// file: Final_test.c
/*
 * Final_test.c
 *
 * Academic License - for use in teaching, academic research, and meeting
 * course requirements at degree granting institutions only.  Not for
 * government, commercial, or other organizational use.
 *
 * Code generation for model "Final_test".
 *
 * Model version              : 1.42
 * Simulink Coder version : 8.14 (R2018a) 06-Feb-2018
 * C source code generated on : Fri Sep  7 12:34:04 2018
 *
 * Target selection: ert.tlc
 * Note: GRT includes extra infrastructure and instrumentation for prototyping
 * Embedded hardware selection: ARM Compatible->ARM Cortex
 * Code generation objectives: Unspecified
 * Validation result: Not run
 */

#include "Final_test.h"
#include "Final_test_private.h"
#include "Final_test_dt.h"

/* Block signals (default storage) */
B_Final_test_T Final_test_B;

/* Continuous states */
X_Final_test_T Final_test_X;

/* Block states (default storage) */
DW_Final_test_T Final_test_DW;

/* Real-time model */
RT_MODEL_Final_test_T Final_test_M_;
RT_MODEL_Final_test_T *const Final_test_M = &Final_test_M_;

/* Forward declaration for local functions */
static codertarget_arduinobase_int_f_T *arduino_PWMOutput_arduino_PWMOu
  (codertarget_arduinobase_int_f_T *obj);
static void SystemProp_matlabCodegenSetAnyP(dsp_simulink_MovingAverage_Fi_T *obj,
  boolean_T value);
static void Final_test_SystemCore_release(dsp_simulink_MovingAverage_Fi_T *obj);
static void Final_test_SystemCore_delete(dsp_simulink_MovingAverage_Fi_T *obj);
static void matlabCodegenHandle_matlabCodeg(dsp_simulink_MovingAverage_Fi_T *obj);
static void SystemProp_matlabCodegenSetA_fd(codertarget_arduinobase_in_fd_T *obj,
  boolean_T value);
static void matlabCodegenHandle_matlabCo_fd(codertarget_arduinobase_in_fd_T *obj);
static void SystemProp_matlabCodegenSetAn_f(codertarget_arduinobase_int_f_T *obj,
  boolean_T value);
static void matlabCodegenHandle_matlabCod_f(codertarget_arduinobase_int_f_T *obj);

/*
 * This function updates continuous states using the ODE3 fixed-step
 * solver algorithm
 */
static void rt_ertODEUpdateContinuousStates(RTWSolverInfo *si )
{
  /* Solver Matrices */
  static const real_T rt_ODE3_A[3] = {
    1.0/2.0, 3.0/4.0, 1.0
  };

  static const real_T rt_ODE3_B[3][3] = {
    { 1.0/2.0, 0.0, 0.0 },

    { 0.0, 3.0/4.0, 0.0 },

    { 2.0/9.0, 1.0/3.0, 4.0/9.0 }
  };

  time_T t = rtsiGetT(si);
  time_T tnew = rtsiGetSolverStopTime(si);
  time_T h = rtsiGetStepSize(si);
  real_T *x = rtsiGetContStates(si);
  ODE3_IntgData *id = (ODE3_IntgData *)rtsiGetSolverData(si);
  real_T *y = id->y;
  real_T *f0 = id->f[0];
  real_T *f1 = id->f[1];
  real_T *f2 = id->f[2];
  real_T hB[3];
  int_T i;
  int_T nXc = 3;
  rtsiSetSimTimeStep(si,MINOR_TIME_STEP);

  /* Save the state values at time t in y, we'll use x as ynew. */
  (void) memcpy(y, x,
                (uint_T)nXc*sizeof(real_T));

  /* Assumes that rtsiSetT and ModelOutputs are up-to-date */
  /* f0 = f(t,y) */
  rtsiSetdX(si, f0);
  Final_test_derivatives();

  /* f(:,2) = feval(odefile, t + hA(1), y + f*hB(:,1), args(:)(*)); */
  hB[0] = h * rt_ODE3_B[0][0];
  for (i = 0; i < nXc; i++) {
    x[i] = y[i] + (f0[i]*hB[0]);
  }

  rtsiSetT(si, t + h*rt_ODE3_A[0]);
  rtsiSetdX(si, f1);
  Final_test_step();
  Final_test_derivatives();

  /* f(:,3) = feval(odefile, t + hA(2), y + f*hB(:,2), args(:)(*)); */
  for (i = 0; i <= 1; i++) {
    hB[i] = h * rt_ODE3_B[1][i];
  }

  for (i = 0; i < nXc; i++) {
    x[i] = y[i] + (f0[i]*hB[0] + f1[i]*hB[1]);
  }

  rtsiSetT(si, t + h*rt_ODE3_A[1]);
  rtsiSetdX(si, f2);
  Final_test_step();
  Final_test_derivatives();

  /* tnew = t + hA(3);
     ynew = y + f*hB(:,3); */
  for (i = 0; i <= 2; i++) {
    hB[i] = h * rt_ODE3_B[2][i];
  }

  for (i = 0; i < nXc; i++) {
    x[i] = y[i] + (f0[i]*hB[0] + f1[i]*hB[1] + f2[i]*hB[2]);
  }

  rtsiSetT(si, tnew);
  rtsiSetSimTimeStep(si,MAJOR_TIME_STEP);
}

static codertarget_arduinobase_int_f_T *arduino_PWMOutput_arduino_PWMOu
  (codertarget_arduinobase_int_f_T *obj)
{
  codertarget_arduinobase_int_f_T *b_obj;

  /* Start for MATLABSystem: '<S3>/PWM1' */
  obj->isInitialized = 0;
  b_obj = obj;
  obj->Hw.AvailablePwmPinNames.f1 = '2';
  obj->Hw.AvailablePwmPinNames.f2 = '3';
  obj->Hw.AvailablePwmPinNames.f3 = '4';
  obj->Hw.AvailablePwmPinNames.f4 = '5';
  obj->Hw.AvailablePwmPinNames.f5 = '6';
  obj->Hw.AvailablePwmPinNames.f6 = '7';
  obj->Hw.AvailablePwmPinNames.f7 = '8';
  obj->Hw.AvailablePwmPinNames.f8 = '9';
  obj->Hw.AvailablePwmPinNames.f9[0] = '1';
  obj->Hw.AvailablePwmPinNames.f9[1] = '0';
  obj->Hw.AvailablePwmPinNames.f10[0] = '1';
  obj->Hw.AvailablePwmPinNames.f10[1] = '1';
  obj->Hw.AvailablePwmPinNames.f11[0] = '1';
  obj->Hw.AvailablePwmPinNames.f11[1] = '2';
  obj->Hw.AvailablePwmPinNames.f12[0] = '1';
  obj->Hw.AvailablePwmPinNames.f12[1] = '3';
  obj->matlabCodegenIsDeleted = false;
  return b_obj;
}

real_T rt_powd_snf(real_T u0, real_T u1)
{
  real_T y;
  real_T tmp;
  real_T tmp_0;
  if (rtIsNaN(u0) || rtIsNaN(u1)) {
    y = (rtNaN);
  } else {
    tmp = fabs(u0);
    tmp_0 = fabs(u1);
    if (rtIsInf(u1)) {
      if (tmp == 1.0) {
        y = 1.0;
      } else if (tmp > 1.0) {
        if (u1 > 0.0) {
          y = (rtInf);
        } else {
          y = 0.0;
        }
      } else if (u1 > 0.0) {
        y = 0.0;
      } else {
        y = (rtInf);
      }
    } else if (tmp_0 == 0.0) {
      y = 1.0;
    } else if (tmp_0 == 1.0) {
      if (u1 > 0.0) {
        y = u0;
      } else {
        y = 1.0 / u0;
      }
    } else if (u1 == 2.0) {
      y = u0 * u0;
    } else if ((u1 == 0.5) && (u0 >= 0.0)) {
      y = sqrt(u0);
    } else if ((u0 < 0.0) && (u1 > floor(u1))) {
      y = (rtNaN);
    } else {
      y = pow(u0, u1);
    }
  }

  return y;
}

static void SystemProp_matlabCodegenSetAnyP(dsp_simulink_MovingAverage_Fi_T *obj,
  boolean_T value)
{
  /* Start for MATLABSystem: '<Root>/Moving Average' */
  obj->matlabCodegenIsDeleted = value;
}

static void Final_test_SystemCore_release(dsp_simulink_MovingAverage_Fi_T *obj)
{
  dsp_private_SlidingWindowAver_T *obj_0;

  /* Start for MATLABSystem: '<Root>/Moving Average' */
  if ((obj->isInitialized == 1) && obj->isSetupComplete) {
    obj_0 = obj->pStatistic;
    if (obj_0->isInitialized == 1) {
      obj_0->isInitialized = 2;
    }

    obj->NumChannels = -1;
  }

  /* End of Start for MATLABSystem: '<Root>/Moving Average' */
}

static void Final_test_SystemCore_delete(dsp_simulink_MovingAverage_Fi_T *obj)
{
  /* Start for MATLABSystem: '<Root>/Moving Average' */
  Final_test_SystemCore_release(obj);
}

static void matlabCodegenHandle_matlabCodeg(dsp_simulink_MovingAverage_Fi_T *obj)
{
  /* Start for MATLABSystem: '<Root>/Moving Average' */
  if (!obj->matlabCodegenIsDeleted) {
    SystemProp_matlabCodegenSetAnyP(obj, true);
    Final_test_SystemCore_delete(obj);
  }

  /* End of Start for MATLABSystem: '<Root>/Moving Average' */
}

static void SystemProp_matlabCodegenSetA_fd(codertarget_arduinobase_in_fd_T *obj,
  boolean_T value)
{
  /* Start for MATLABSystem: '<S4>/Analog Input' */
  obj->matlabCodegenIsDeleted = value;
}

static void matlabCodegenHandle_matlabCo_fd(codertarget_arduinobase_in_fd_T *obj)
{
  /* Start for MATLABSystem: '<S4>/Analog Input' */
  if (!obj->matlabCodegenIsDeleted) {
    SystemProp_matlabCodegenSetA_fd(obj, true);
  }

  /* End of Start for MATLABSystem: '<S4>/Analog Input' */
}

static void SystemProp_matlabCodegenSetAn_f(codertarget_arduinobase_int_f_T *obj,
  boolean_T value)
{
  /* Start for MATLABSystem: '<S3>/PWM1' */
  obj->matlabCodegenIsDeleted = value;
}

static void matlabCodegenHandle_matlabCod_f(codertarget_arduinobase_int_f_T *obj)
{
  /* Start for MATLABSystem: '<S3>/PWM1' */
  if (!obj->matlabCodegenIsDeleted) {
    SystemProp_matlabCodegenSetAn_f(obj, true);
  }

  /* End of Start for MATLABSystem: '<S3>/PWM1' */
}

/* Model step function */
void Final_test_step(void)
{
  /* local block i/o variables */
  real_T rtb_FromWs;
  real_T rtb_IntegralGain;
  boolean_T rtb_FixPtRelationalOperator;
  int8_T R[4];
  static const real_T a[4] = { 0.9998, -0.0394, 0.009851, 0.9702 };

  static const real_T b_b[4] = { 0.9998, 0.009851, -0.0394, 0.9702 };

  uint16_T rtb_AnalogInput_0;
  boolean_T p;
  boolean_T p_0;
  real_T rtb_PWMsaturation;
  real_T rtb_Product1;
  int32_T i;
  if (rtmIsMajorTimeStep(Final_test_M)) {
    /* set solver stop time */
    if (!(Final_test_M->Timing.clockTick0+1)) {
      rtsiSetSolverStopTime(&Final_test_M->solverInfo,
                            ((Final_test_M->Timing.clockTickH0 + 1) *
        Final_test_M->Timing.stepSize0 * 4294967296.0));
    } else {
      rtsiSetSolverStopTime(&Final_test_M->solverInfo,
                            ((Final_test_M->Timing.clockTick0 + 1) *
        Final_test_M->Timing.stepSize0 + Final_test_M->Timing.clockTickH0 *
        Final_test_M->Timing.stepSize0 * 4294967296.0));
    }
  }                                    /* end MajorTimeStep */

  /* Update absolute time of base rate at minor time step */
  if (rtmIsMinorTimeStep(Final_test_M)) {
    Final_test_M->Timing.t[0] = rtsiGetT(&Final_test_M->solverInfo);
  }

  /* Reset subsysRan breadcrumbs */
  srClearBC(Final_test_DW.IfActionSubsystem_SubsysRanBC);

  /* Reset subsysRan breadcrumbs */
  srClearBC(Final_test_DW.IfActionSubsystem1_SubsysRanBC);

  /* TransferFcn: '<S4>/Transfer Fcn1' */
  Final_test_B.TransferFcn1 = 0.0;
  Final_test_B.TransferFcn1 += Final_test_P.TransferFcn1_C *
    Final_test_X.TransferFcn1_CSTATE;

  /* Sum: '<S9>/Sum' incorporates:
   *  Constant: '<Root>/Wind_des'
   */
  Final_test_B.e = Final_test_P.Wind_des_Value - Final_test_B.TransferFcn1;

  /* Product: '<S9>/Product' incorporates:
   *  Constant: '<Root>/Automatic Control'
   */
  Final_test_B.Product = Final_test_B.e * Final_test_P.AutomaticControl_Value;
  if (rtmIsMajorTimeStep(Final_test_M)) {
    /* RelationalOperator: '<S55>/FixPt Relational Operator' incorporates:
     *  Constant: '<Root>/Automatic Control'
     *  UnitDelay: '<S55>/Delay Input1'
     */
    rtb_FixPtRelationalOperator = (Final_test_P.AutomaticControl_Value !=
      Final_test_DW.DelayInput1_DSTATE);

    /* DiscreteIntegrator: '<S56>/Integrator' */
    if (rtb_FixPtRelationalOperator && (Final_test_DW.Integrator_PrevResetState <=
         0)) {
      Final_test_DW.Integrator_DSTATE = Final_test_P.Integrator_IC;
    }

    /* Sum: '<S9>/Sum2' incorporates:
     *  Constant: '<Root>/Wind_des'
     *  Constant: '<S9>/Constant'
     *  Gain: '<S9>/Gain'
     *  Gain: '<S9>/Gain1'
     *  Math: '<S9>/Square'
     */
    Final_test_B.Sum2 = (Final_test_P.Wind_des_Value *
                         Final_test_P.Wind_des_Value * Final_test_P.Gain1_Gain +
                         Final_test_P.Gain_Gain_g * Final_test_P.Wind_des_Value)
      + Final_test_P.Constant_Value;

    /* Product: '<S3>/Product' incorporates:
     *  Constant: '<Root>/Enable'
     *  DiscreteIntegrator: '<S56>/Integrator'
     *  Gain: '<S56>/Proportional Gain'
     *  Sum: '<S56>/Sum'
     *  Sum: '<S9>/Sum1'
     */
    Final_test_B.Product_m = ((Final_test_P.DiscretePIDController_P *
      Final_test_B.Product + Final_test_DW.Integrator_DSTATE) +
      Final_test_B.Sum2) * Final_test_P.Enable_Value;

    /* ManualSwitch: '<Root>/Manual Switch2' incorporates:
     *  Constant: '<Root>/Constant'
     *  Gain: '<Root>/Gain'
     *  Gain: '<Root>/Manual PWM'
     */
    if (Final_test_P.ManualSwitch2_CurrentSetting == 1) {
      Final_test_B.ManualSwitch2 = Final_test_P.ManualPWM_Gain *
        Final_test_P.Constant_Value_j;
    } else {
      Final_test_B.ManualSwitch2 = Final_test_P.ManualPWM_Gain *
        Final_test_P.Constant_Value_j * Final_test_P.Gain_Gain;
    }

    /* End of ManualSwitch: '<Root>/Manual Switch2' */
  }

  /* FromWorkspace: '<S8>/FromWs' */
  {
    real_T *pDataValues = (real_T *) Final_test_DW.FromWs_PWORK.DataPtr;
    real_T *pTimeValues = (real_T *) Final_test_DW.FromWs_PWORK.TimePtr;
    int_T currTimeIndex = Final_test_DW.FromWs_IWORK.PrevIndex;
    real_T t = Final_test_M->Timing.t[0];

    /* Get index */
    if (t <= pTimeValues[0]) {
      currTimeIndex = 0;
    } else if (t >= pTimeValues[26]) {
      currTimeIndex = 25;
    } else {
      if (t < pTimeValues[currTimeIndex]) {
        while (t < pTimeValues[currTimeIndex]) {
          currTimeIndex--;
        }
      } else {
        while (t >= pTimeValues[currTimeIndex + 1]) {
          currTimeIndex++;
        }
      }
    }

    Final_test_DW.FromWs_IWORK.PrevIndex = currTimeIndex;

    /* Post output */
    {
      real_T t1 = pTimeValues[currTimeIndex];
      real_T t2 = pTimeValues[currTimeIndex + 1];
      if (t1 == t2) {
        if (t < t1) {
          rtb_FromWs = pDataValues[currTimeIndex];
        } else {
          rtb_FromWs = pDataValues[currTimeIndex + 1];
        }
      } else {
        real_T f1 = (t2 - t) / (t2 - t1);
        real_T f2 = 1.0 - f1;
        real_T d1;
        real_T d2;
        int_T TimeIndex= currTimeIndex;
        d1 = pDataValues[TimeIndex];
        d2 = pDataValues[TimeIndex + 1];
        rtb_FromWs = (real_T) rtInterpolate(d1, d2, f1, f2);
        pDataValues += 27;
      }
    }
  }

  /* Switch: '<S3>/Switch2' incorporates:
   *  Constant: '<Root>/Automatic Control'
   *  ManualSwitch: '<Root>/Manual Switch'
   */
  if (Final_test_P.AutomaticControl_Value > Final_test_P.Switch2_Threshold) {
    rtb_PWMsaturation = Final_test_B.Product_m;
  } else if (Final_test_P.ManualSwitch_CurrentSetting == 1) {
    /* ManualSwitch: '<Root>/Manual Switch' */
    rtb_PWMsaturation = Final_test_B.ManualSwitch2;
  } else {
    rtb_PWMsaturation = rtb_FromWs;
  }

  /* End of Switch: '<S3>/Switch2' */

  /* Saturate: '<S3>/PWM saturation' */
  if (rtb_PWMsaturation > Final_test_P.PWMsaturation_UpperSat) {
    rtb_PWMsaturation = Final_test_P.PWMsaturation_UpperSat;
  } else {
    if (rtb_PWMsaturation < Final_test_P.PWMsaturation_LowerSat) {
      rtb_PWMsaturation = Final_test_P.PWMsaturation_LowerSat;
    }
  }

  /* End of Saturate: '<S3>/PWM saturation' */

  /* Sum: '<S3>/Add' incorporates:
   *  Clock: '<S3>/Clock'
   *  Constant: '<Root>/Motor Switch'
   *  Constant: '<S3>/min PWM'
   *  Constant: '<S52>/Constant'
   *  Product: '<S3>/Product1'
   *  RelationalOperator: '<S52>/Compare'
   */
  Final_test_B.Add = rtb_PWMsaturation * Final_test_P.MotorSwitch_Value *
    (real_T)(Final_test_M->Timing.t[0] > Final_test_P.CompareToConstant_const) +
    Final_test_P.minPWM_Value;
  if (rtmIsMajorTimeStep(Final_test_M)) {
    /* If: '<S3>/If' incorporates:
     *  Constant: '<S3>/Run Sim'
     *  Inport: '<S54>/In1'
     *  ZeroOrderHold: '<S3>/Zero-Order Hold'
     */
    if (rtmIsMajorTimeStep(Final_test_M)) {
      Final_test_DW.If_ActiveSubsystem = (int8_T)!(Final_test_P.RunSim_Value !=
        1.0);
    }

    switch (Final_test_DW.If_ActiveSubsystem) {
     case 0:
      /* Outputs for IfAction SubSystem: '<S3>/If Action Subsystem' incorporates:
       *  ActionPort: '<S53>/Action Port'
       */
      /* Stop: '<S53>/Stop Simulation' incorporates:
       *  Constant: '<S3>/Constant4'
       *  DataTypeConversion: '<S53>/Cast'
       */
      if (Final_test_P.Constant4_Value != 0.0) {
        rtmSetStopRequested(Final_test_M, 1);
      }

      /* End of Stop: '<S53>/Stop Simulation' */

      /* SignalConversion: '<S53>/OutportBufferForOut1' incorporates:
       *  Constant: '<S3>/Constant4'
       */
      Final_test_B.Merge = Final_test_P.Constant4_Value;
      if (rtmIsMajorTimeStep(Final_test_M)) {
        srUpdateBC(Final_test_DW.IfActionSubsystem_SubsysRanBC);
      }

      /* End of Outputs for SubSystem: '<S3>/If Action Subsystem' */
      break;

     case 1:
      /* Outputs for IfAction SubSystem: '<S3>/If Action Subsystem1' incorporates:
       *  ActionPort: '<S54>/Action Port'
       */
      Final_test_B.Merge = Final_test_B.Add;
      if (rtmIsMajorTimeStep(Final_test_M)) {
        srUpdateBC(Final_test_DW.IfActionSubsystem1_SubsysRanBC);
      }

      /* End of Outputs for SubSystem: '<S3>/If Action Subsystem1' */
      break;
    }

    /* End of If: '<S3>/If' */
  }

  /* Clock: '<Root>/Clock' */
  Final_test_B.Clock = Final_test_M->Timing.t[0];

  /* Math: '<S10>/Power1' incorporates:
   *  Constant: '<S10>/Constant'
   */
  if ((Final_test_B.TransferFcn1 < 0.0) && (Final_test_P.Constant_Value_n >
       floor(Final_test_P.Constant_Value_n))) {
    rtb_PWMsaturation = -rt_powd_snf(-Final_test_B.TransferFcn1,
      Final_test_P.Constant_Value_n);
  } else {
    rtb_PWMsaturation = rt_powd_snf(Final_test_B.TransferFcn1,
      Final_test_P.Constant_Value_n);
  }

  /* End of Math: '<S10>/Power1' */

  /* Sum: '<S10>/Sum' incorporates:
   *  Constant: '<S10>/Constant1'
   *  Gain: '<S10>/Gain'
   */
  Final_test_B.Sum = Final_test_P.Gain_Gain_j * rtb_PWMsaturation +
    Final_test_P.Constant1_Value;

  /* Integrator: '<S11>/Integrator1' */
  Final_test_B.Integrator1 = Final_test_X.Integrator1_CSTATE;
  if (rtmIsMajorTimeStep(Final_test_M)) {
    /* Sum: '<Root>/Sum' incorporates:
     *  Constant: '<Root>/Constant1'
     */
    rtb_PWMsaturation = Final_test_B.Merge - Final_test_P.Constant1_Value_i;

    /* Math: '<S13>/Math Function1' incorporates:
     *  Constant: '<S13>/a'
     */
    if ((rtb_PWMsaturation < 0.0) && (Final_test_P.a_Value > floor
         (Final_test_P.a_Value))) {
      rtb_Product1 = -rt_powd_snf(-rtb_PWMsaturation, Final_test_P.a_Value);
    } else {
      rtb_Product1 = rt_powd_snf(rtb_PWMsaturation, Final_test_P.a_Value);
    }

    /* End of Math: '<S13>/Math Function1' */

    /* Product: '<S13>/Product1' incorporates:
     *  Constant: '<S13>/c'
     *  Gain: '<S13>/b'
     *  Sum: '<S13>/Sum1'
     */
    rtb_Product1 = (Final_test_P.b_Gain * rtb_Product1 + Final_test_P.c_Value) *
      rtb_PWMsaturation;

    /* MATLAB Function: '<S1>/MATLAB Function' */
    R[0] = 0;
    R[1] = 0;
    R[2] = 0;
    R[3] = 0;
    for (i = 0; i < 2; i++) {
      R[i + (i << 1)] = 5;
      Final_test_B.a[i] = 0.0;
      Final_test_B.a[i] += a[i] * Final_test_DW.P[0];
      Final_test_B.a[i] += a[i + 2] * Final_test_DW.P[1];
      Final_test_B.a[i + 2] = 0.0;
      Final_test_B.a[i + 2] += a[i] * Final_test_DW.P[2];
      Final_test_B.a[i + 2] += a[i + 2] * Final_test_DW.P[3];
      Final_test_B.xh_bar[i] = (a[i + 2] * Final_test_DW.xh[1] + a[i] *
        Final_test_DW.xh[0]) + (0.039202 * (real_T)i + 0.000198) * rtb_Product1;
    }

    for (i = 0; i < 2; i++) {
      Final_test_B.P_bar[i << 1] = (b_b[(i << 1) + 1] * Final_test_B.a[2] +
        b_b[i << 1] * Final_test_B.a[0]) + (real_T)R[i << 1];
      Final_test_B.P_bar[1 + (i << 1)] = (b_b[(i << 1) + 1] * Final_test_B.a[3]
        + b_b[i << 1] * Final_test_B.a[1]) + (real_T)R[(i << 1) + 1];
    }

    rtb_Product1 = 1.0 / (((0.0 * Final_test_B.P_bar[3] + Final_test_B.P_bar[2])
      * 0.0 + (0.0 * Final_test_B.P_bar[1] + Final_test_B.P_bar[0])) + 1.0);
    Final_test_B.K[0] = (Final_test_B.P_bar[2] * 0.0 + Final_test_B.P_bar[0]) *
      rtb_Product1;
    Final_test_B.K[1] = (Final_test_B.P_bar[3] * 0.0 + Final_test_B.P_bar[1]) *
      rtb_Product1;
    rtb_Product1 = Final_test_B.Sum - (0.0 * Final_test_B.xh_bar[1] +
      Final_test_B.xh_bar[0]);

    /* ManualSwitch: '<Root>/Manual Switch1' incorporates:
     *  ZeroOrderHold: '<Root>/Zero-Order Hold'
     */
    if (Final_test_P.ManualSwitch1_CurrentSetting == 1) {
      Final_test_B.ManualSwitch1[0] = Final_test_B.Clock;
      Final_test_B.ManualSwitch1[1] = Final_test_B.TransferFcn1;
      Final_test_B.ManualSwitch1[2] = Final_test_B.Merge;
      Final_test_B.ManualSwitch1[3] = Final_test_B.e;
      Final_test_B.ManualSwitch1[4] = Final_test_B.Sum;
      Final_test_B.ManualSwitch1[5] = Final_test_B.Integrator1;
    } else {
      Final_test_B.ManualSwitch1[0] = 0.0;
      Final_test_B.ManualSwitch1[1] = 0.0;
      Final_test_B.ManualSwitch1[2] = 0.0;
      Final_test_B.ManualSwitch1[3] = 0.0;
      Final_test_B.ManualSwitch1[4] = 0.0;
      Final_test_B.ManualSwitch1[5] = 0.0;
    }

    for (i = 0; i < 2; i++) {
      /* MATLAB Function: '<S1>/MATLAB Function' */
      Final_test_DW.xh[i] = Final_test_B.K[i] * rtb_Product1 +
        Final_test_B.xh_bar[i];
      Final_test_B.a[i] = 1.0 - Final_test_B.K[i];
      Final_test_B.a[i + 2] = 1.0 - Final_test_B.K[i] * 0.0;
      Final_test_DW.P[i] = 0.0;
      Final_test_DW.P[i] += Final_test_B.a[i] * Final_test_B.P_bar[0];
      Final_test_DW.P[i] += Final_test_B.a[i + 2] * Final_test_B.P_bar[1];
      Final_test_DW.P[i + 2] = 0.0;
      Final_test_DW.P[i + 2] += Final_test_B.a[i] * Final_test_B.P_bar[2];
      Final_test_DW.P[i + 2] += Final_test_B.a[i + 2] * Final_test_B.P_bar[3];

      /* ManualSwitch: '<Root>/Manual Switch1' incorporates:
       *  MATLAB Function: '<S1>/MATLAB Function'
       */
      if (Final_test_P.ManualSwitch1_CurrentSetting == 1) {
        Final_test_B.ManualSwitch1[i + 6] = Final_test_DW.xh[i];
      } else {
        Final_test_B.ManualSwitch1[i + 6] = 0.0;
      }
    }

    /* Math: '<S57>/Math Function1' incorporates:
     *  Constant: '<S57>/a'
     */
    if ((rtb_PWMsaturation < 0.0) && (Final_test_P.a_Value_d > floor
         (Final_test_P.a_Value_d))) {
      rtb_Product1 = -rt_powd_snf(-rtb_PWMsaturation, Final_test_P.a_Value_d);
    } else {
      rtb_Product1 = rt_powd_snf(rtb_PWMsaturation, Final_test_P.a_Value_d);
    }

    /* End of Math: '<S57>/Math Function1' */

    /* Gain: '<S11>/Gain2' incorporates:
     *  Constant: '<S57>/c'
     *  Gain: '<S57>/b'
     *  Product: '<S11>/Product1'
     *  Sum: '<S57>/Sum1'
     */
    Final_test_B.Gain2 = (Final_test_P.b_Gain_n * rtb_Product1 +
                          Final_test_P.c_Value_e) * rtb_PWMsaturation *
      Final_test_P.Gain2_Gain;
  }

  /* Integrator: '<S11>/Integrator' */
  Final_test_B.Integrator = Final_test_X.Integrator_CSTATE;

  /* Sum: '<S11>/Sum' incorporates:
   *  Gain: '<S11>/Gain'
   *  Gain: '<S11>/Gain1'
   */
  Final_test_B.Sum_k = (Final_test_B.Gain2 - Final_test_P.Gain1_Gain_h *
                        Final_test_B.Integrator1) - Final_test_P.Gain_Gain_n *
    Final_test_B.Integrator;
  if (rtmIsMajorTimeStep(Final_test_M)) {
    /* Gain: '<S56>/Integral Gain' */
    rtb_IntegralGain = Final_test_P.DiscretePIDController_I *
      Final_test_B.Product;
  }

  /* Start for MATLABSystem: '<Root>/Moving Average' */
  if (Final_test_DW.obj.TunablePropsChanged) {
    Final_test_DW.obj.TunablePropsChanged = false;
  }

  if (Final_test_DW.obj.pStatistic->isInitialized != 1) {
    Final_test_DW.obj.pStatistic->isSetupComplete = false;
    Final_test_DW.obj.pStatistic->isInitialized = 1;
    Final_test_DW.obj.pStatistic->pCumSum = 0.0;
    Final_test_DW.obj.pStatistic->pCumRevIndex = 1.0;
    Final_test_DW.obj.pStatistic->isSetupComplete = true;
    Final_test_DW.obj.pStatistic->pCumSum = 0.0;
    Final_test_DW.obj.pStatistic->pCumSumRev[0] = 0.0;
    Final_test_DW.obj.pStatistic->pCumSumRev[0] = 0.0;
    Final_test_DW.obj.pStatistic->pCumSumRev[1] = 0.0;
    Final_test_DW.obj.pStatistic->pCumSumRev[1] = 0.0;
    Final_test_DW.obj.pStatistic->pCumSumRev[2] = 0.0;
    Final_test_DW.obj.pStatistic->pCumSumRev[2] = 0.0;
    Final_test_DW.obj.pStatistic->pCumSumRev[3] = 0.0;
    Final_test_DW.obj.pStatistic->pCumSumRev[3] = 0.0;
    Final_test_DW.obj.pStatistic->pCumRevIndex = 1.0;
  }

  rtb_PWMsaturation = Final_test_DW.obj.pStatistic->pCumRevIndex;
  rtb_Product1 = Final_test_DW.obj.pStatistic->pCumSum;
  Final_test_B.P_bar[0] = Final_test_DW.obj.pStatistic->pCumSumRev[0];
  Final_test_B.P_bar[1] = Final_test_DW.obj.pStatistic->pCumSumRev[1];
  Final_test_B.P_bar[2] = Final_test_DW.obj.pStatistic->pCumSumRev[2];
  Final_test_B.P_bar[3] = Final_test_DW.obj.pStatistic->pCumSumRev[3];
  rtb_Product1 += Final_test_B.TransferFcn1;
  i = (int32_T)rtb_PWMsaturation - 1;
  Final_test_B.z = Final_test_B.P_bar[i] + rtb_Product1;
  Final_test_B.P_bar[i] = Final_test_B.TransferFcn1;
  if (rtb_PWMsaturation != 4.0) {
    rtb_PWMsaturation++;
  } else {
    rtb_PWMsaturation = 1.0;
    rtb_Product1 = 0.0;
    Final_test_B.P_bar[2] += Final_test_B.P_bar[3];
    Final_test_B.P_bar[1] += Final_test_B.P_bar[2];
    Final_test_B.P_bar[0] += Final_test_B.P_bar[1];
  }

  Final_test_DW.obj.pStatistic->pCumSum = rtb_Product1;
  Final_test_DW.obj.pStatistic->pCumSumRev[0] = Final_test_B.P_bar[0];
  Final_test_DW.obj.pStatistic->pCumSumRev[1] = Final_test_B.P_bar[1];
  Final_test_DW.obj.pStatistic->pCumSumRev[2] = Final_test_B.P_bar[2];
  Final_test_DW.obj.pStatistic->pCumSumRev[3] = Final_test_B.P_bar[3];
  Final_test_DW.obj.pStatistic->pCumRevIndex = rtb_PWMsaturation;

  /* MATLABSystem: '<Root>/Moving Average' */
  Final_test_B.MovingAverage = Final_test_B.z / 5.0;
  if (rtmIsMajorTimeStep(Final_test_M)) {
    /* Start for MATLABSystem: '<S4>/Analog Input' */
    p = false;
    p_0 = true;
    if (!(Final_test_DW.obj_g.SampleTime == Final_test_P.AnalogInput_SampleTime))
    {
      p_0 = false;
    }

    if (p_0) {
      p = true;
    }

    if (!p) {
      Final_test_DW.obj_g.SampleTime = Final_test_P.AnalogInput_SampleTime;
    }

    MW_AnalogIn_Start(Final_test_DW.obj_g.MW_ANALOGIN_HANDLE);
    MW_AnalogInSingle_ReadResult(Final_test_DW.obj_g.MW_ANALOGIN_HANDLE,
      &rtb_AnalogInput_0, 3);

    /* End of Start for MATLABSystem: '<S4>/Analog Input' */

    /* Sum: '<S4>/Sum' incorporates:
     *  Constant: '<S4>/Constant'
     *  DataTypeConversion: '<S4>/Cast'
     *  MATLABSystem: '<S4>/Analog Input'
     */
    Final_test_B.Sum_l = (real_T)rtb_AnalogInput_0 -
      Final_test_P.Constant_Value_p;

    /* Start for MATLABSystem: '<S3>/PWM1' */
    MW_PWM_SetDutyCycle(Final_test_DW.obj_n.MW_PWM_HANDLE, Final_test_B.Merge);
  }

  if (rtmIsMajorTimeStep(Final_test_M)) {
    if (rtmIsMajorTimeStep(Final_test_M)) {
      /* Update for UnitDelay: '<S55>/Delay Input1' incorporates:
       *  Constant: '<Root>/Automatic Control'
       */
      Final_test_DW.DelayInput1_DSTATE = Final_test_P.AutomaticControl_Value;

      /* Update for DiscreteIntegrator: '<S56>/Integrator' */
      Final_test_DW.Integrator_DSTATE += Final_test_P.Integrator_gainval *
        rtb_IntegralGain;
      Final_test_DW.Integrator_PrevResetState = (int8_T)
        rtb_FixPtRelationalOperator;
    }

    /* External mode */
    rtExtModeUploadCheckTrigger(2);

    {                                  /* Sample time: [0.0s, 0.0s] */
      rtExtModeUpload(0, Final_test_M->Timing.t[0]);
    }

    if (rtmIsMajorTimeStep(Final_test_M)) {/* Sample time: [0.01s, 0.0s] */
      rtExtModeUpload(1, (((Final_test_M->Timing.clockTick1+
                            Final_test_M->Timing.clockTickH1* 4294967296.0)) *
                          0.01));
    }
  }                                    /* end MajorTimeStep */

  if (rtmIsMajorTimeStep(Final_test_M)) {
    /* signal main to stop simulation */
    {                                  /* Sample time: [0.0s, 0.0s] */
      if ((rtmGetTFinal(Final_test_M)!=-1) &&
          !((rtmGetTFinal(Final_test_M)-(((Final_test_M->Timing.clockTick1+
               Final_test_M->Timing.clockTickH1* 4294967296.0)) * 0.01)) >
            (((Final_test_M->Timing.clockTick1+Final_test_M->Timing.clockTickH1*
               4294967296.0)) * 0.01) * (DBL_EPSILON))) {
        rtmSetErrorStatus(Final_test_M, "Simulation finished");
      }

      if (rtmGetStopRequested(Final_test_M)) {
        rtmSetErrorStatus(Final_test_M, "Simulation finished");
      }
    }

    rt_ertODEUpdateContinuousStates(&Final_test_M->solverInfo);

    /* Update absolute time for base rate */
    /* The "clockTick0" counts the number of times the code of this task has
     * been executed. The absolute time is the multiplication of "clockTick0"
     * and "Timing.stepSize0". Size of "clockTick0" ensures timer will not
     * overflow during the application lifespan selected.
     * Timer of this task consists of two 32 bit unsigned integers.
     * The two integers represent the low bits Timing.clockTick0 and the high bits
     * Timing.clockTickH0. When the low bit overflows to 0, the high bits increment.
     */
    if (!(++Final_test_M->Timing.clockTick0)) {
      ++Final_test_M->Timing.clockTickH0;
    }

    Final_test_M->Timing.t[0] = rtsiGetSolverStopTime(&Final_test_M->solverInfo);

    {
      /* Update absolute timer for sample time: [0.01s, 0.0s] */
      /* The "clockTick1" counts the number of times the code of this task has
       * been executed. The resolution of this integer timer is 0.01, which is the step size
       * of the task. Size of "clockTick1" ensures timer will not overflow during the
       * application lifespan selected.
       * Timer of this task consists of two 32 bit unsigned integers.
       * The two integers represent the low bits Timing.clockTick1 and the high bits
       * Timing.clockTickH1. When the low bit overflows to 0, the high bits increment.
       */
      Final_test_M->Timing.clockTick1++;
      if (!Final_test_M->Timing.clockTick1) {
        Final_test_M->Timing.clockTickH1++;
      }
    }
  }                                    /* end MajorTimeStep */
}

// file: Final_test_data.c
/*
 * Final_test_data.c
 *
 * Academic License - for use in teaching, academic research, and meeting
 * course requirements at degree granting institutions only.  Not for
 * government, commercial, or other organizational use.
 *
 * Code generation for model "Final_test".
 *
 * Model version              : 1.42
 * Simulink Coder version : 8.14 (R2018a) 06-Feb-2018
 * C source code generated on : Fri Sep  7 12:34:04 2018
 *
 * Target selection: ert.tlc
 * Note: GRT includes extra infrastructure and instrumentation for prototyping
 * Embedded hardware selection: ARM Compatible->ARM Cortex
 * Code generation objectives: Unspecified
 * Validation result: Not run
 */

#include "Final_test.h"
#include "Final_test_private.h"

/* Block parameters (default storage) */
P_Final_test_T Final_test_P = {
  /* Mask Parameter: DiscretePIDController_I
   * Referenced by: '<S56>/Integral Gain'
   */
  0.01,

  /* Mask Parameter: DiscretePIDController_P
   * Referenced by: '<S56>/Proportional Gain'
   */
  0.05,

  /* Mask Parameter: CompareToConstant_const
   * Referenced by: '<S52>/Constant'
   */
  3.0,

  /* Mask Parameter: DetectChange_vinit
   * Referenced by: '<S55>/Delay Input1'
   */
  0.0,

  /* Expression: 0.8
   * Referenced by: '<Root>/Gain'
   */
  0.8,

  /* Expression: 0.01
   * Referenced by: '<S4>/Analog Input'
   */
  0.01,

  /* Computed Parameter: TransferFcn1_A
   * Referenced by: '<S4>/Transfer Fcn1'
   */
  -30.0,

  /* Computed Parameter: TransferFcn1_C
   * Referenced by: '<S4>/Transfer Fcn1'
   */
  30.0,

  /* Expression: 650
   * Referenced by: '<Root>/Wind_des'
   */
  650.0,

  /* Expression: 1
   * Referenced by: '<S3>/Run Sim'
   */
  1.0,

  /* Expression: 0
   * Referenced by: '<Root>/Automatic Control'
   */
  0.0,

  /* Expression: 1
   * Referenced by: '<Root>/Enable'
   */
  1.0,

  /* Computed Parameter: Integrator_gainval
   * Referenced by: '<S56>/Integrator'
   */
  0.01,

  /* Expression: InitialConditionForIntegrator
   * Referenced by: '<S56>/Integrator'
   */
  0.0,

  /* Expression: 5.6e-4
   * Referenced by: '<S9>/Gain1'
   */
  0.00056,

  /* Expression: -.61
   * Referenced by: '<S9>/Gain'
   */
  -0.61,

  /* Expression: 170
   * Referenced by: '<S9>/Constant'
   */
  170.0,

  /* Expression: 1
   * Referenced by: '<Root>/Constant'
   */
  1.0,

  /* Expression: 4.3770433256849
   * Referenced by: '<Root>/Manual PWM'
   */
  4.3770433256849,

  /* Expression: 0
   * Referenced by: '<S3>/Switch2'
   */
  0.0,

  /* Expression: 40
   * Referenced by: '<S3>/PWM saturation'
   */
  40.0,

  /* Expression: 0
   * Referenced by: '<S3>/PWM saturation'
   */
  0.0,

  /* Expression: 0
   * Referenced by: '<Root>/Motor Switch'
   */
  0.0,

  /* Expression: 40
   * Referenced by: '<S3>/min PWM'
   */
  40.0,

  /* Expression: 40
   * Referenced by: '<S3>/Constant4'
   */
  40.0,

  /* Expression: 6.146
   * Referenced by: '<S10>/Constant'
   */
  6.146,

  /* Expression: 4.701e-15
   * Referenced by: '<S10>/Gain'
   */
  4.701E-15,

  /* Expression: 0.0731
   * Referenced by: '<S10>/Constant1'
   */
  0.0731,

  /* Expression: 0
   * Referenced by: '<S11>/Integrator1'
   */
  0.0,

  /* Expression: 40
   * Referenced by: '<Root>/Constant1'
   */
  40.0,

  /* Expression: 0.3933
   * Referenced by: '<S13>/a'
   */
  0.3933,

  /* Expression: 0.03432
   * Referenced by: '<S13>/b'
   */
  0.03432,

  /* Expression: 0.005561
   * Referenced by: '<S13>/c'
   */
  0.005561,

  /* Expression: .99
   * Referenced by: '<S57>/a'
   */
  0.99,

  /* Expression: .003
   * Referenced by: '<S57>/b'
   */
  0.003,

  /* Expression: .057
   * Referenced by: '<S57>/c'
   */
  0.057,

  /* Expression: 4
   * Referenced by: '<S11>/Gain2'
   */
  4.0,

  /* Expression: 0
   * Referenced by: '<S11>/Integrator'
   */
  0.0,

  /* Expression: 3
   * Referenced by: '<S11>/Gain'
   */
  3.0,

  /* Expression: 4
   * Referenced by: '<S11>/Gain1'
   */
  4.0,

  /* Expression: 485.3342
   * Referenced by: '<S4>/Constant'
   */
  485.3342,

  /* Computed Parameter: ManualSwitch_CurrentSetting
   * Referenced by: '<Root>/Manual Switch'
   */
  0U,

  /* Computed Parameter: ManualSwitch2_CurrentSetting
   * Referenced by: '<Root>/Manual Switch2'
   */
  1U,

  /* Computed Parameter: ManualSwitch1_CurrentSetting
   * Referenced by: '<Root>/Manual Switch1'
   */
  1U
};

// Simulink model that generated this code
simulink model "Final_test"  (R2018a)
settings: Solver=FixedStepAuto  StartTime=0.0  StopTime=inf  FixedStep=0.01  RelTol=1e-3  EnableMultiTasking=on
InitFcn:
  | set_param('Final_test/Output/Run Sim','Value','1');
  | set_param('Final_test/Motor Switch','Value','0');
  | set_param('Final_test/Automatic Control','Value','0');
  | %set_param('Final_test/Manual PWM','Gain','0');
undefined symbols (not defined in the file or in its folder): Discrete, sigbuilder_block, Time
libraries: simulink x3, arduinolib x3, ctrlSharedLib x1, dspstat3 x1

== system Final_test ==
  Automatic Control : Constant  Value=0  SampleTime=0.01
  Cast : DataTypeConversion  OutDataTypeStr=double
  Clock : Clock
  Constant : Constant  SampleTime=0.01
  Constant1 : Constant  Value=40
  Demux : Demux  Outputs=6
  Display : Display
  Display1 : Display
  Enable : Constant  SampleTime=0.01
  Gain : Gain  Gain=0.8
  Kalman Filter : Subsystem
  Kalman Filter1 : ctrlSharedLib/Kalman Filter  Commented=on  TimeDomain=Discrete-Time  UseCurrentEstimator=on  ModelSource=Individual A, B, C, D matrices  ModelSourceVariable=ss(0.95,1,1,0,1)  A="[0.9998  0.009851; -0.0394    0.9702]"  B=[0.000198; 0.0394]  C=[1 0]  D=0  NumberOfStates=1  NumberOfInputs=1  NumberOfOutputs=1  InitialEstimateSource=Dialog  X0=0  P0=10  UseK=off  UseGH=off  NumberOfProcessNoiseInputs=1  G=1  TimeInvariantG=on  H=0  TimeInvariantH=on  Q=1  TimeInvariantQ=on  R=5  TimeInvariantR=on  N=0  TimeInvariantN=on  AddInputPort=on  AddEnablePort=off  OutputEstimatedY=off  OutputP=off  Ts=-1
  Knob : Subsystem  DialogController=hmiCreateDDGDialog  IsWebBlock=on  mask(MWDashboardBlock){webBlockId=852d3d9e-f600-4180-8955-96c4171a0510, webBlockType=continuousknob, ShowInLibBrowser=on, ShowInitialText=on, HMISrcModelName=Final_test}
      mask prompts: webBlockId "WebBlock Id"; webBlockType "WebBlock Type"; HMISrcModelName "Source Model"
      mask help: SimulinkHMI:dialogs:ContinuousKnobDialogDesc
  Manual PWM : Gain  Gain=4.3770433256849
  Manual Switch : ManualSwitch  CurrentSetting=0
  Manual Switch1 : ManualSwitch
  Manual Switch2 : ManualSwitch
  Motor Switch : Constant  Value=0  SampleTime=0.01
  Moving Average : dspstat3/Moving Average  Method=Sliding window  ForgettingFactorPort=off  SpecifyWindowLength=on  WindowLength=5  ForgettingFactor=0.9  SimulateUsing=Code generation
  Mux : Mux  Inputs=7
  Output : Subsystem
  Radio Button : RadioButtonGroup  WebBlockId=124  SelectedLabel=OFF  ButtonGroupName=SIM STATUS
  Radio Button1 : RadioButtonGroup  WebBlockId=141  SelectedLabel=OFF  ButtonGroupName=SIM STATUS
  Radio Button2 : RadioButtonGroup  WebBlockId=144  SelectedLabel=OFF  ButtonGroupName=SIM STATUS
  Scope : Scope  NumInputPorts=4
  Scope1 : Scope
  Sensor : Subsystem
  Slider : Subsystem  DialogController=hmiCreateDDGDialog  IsWebBlock=on  mask(MWDashboardBlock){webBlockId=6d6bce73-9061-4720-a103-f9820fa904f8, webBlockType=slider, ShowInLibBrowser=on, ShowInitialText=on, HMISrcModelName=Final_test}
      mask prompts: webBlockId "WebBlock Id"; webBlockType "WebBlock Type"; HMISrcModelName "Source Model"
      mask help: SimulinkHMI:dialogs:SliderDialogDesc
  Slider1 : Subsystem  DialogController=hmiCreateDDGDialog  IsWebBlock=on  mask(MWDashboardBlock){webBlockId=583235cf-a666-476d-a93b-c374fcd1b609, webBlockType=slider, ShowInLibBrowser=on, ShowInitialText=on, HMISrcModelName=Final_test}
      mask prompts: webBlockId "WebBlock Id"; webBlockType "WebBlock Type"; HMISrcModelName "Source Model"
      mask help: SimulinkHMI:dialogs:SliderDialogDesc
  Step : Subsystem  Tag=STV Subsys  LoadFcn=sigbuilder_block('load');  StartFcn=sigbuilder_block('start');  StopFcn=sigbuilder_block('stop');  ClipboardFcn=sigbuilder_block('clipboard');  mask(Sigbuilder block){tuvar=[0:10]}
      mask help: Simulink:masks:SigbuilderBlock_MD
      mask init:
      | if ~strcmp(get_param(bdroot(gcbh),'SimulationStatus'),'stopped') tuvar = sigbuilder_block('maskInit'); end
  Step1 : Subsystem  Tag=STV Subsys  LoadFcn=sigbuilder_block('load');  StartFcn=sigbuilder_block('start');  StopFcn=sigbuilder_block('stop');  ClipboardFcn=sigbuilder_block('clipboard');  mask(Sigbuilder block){tuvar=[0:10]}
      mask help: Simulink:masks:SigbuilderBlock_MD
      mask init:
      | if ~strcmp(get_param(bdroot(gcbh),'SimulationStatus'),'stopped') tuvar = sigbuilder_block('maskInit'); end
  Step2 : Subsystem  Tag=STV Subsys  LoadFcn=sigbuilder_block('load');  StartFcn=sigbuilder_block('start');  StopFcn=sigbuilder_block('stop');  ClipboardFcn=sigbuilder_block('clipboard');  mask(Sigbuilder block){tuvar=[0:10]}
      mask help: Simulink:masks:SigbuilderBlock_MD
      mask init:
      | if ~strcmp(get_param(bdroot(gcbh),'SimulationStatus'),'stopped') tuvar = sigbuilder_block('maskInit'); end
  Step3 : Subsystem  Tag=STV Subsys  LoadFcn=sigbuilder_block('load');  StartFcn=sigbuilder_block('start');  StopFcn=sigbuilder_block('stop');  ClipboardFcn=sigbuilder_block('clipboard');  mask(Sigbuilder block){tuvar=[0:10]}
      mask help: Simulink:masks:SigbuilderBlock_MD
      mask init:
      | if ~strcmp(get_param(bdroot(gcbh),'SimulationStatus'),'stopped') tuvar = sigbuilder_block('maskInit'); end
  Subsystem1 : Subsystem
  Subsystem2 : Subsystem
  Sum : Sum  Inputs=|+-
  Terminator : Terminator
  Thrust Model : Subsystem
  To Workspace : ToWorkspace  VariableName=Data  SampleTime=-1
  Wind_des : Constant  Value=650  SampleTime=0.01
  Zero-Order Hold : ZeroOrderHold  SampleTime=0.01
  wires:
  Motor Switch/1 -> Output/3(Main Switch)
  Enable/1 -> Output/1(Enable)
  Constant/1 -> Manual PWM/1
  Wind_des/1 -> Subsystem1/2(Wind des)
  Subsystem1/1(PWM) -> Output/4(PWM)
  Automatic Control/1 -> Subsystem1/1(Automatic Control), Output/2(Automatic Enable)
  Sensor/1(Wind) -> Subsystem1/3(Wind)
  Mux/1 -> Zero-Order Hold/1
  [Wind_filt] -> Mux/2
  [PWM] -> Mux/3
  [error] -> Mux/4
  Clock/1 -> Cast/1
  Cast/1 -> Mux/1
  Manual Switch/1 -> Output/5(Manual PWM)
  Manual Switch1/1 -> Demux/1, To Workspace/1
  Zero-Order Hold/1 -> Manual Switch1/1
  Demux/2 -> Scope/1  "Wind"
  Demux/5 -> Scope/4  "Sync"
  Demux/4 -> Scope/3  "Error"
  Demux/3 -> Scope/2  "PWM"
  Demux/1 -> Terminator/1
  Constant1/1 -> Sum/2
  Sum/1 -> Kalman Filter1/1, Kalman Filter/1(pwm), Thrust Model/1(pwm)
  [Wind_filt] -> Subsystem2/1(In1)
  Thrust Model/1(Thrust) -> Mux/6
  [PWM] -> Sum/1
  Moving Average/1 -> Scope1/1, Display1/1
  [Wind_filt] -> Moving Average/1
  [PWM] -> Display/1
  Kalman Filter/1(Wind estimate) -> Mux/7
  Manual PWM/1 -> Gain/1, Manual Switch2/1
  Gain/1 -> Manual Switch2/2
  Manual Switch2/1 -> Manual Switch/1
  Subsystem2/2("power ") -> Kalman Filter/2(Wind_thrust), Mux/5
  Step3/1(Signal 2) -> Manual Switch/2

== system Final_test/Kalman Filter ==
  pwm : Inport
  Wind_thrust : Inport  Port=2
  MATLAB Function : MATLAB Function  TreatAsAtomicUnit=on
  Subsystem1 : Subsystem
  Wind estimate : Outport
  wires:
  Subsystem1/1(u) -> MATLAB Function/1(u)
  Wind_thrust/1 -> MATLAB Function/2(y)
  pwm/1 -> Subsystem1/1(PWM)
  MATLAB Function/1(xest) -> Wind estimate/1

== system Final_test/Knob ==

== system Final_test/Output ==
  Enable : Inport
  Automatic Enable : Inport  Port=2
  Main Switch : Inport  Port=3
  PWM : Inport  Port=4
  Manual PWM : Inport  Port=5
  Add : Sum
  Clock : Clock
  Compare To Constant : simulink/Logic and Bit Operations/Compare To Constant  relop=>  const=3  OutDataTypeStr=boolean
  Constant4 : Constant  Value=40  SampleTime=0.01
  If : If  IfExpression=u1 ~= 1
  If Action Subsystem : Subsystem  TreatAsAtomicUnit=on
  If Action Subsystem1 : Subsystem  TreatAsAtomicUnit=on
  Merge : Merge
  PWM saturation : Saturate  UpperLimit=40  LowerLimit=0
  PWM1 : arduinolib/PWM  pinNumber=12  EnableInputFrequency=off  InitialFrequency=2000  InitialDutyCycle=0  NotificationType=None  blockPlatform=arduino
  Product : Product
  Product1 : Product  Inputs=3
  RT : RateTransition  OutPortSampleTime=0.01
  RT1 : RateTransition  OutPortSampleTime=0.01
  RT2 : RateTransition  OutPortSampleTime=0.01
  Run Sim : Constant  Value=0  SampleTime=0.01
  Switch2 : Switch  Criteria=u2 > Threshold
  Zero-Order Hold : ZeroOrderHold  SampleTime=0.01
  min PWM : Constant  Value=40  SampleTime=0.01
  tag scope: PWM=global
  wires:
  Clock/1 -> Compare To Constant/1
  min PWM/1 -> RT1/1
  Compare To Constant/1 -> Product1/3
  Automatic Enable/1 -> RT2/1
  Manual PWM/1 -> Switch2/3
  PWM/1 -> Product/2
  Switch2/1 -> PWM saturation/1
  Main Switch/1 -> RT/1
  Product1/1 -> Add/1
  PWM saturation/1 -> Product1/1
  Product/1 -> Switch2/1
  Enable/1 -> Product/1
  If/1 -> If Action Subsystem/Action
  Run Sim/1 -> If/1
  Constant4/1 -> If Action Subsystem/1(In1)
  Add/1 -> Zero-Order Hold/1
  If/2 -> If Action Subsystem1/Action
  If Action Subsystem1/1(Out1) -> Merge/2
  Merge/1 -> [PWM], PWM1/1
  Zero-Order Hold/1 -> If Action Subsystem1/1(In1)
  RT/1 -> Product1/2
  RT1/1 -> Add/2
  RT2/1 -> Switch2/2
  If Action Subsystem/1(Out1) -> Merge/1

== system Final_test/Sensor ==
  Analog Input : arduinolib/Analog Input  pinNumber=2  ReadResultsOnly=off  ConversionTriggerSource=Software  ExternalTriggerType=uint32(0)  OutputDataType=uint16  EnableConversionCompleteNotify=off  EnableOuputStatus=off  SampleTime=0.01  blockPlatform=arduino
  Analog Input1 : arduinolib/Analog Input  Commented=on  pinNumber=3  ReadResultsOnly=off  ConversionTriggerSource=Software  ExternalTriggerType=uint32(0)  OutputDataType=uint16  EnableConversionCompleteNotify=off  EnableOuputStatus=off  SampleTime=0.01  blockPlatform=arduino
  Cast : DataTypeConversion  OutDataTypeStr=double
  Cast1 : DataTypeConversion  Commented=on  OutDataTypeStr=double
  Constant : Constant  Value=485.3342
  Goto1 : Goto  Commented=on  GotoTag=sync  TagVisibility=global
  Mux1 : Mux  Inputs=2
  Scope1 : Scope
  Scope4 : Scope  Commented=on
  Sum : Sum  Inputs=|+-
  Transfer Fcn1 : TransferFcn  Numerator=[30]  Denominator=[1 30]
  Zero-Order Hold : ZeroOrderHold  Commented=on  SampleTime=0.01
  Zero-Order Hold1 : ZeroOrderHold  SampleTime=0.01
  Wind : Outport
  tag scope: Wind=global, Wind_filt=global
  wires:
  Zero-Order Hold/1 -> Cast1/1, Scope4/1
  Analog Input/1 -> Cast/1
  Cast/1 -> Zero-Order Hold1/1
  Analog Input1/1 -> Zero-Order Hold/1
  Cast1/1 -> Goto1/1
  Zero-Order Hold1/1 -> Sum/1
  Transfer Fcn1/1 -> Mux1/1, [Wind_filt], Wind/1
  Mux1/1 -> Scope1/1
  Constant/1 -> Sum/2
  Sum/1 -> Mux1/2, Transfer Fcn1/1

== system Final_test/Slider ==

== system Final_test/Slider1 ==

== system Final_test/Step ==
  Demux : Demux  Tag=STV Demux  Outputs=1
  FromWs : FromWorkspace  Tag=STV FromWs  VariableName=tuvar  SampleTime=0
  Signal 2 : Outport  Tag=STV Outport
  wires:
  FromWs/1 -> Demux/1
  Demux/1 -> Signal 2/1

== system Final_test/Step1 ==
  Demux : Demux  Tag=STV Demux  Outputs=1
  FromWs : FromWorkspace  Tag=STV FromWs  VariableName=tuvar  SampleTime=0
  Signal 2 : Outport  Tag=STV Outport
  wires:
  Demux/1 -> Signal 2/1
  FromWs/1 -> Demux/1

== system Final_test/Step2 ==
  Demux : Demux  Tag=STV Demux  Outputs=1
  FromWs : FromWorkspace  Tag=STV FromWs  VariableName=tuvar  SampleTime=0
  Signal 1 : Outport  Tag=STV Outport
  wires:
  FromWs/1 -> Demux/1
  Demux/1 -> Signal 1/1

== system Final_test/Step3 ==
  Demux : Demux  Tag=STV Demux  Outputs=1
  FromWs : FromWorkspace  Tag=STV FromWs  VariableName=tuvar  SampleTime=0
  Signal 2 : Outport  Tag=STV Outport
  wires:
  FromWs/1 -> Demux/1
  Demux/1 -> Signal 2/1

== system Final_test/Subsystem1 ==
  Automatic Control : Inport
  Wind des : Inport  Port=2
  Wind : Inport  Port=3
  Constant : Constant  Value=170
  Detect Change : simulink/Logic and Bit Operations/Detect Change  vinit=0  OutDataTypeStr=boolean
  Discrete PID Controller : simulink/Continuous/PID Controller  Controller=PI  TimeDomain=Discrete-time  SampleTime=0.01  IntegratorMethod=Forward Euler  FilterMethod=Forward Euler  Form=Parallel  UseFilter=on  ControllerParametersSource=internal  P=0.05  I=0.01  D=0  N=100  InitialConditionSource=internal  InitialConditionForIntegrator=0  InitialConditionForFilter=0  ExternalReset=rising  LimitOutput=off  UpperSaturationLimit=inf  LowerSaturationLimit=-inf  LinearizeAsGain=off  AntiWindupMode=none  Kb=1  TrackingMode=off  Kt=1  PParamMin=[]  PParamMax=[]  IParamMin=[]  IParamMax=[]  DParamMin=[]  DParamMax=[]  NParamMin=[]  NParamMax=[]  KbParamMin=[]  KbParamMax=[]  KtParamMin=[]  KtParamMax=[]  POutMin=[]  POutMax=[]  IOutMin=[]  IOutMax=[]  DOutMin=[]  DOutMax=[]  NOutMin=[]  NOutMax=[]  KbOutMin=[]  KbOutMax=[]  KtOutMin=[]  KtOutMax=[]  IntegratorOutMin=[]  IntegratorOutMax=[]  FilterOutMin=[]  FilterOutMax=[]  SumOutMin=[]  SumOutMax=[]  SumI1OutMin=[]  SumI1OutMax=[]  SumI2OutMin=[]  SumI2OutMax=[]  SumI3OutMin=[]  SumI3OutMax=[]  SumDOutMin=[]  SumDOutMax=[]  SaturationOutMin=[]  SaturationOutMax=[]  IntegratorContinuousStateAttributes=''  IntegratorStateMustResolveToSignalObject=off  IntegratorRTWStateStorageClass=Auto  FilterContinuousStateAttributes=''  FilterStateMustResolveToSignalObject=off  FilterRTWStateStorageClass=Auto  DifferentiatorICPrevScaledInput=0  DifferentiatorOutMin=[]  DifferentiatorOutMax=[]  FilterDiffOutCoefMin=[]  FilterDiffOutCoefMax=[]  SumDenOutMin=[]  SumDenOutMax=[]  SumNumOutMin=[]  SumNumOutMax=[]  ReciprocalOutMin=[]  ReciprocalOutMax=[]  DivideOutMin=[]  DivideOutMax=[]  TunerSelectOption=Transfer Function Based (PID Tuner App)
  Gain : Gain  Gain=-.61
  Gain1 : Gain  Gain=5.6e-4
  Nominal PWM : Constant  Commented=on  Value=7  SampleTime=0.01
  Product : Product
  Scope : Scope
  Square : Math  Operator=square  SaturateOnIntegerOverflow=on
  Sum : Sum  Inputs=|+-
  Sum1 : Sum  Inputs=|++
  Sum2 : Sum  Inputs=|+++
  PWM : Outport
  tag scope: error=global
  wires:
  Detect Change/1 -> Discrete PID Controller/2
  Wind des/1 -> Gain/1, Square/1, Sum/1
  Discrete PID Controller/1 -> Sum1/1
  Sum/1 -> [error], Product/1  "e"
  Wind/1 -> Sum/2
  Automatic Control/1 -> Product/2, Detect Change/1
  Sum1/1 -> PWM/1
  Product/1 -> Discrete PID Controller/1
  Gain/1 -> Sum2/2
  Gain1/1 -> Sum2/1
  Constant/1 -> Sum2/3
  Square/1 -> Gain1/1
  Sum2/1 -> Sum1/2, Scope/1

== system Final_test/Subsystem2 ==
  In1 : Inport
  Constant : Constant  Value=6.146
  Constant1 : Constant  Value=0.0731
  Gain : Gain  Gain=4.701e-15
  Power : Math  Operator=pow  SaturateOnIntegerOverflow=on
  Power1 : Math  Operator=pow  SaturateOnIntegerOverflow=on
  Sum : Sum  Inputs=|++
  a : Gain  Gain=4.24e-47
  b : Constant  Value=16.36
  "wind_thrust " : Outport
  "power " : Outport  Port=2
  wires:
  b/1 -> Power/2
  Power/1 -> a/1
  a/1 -> "wind_thrust "/1
  In1/1 -> Power1/1, Power/1
  Constant/1 -> Power1/2
  Power1/1 -> Gain/1
  Gain/1 -> Sum/1
  Constant1/1 -> Sum/2
  Sum/1 -> "power "/1

== system Final_test/Thrust Model ==
  pwm : Inport
  Gain : Gain  Gain=3
  Gain1 : Gain  Gain=4
  Gain2 : Gain  Gain=4
  Integrator : Integrator
  Integrator1 : Integrator
  Product1 : Product
  Subsystem : Subsystem
  Sum : Sum  Inputs=+--
  Thrust : Outport
  wires:
  Product1/1 -> Gain2/1
  pwm/1 -> Product1/1, Subsystem/1(Inport1)
  Integrator/1 -> Gain/1, Integrator1/1
  Subsystem/1(Out1) -> Product1/2
  Sum/1 -> Integrator/1
  Integrator1/1 -> Gain1/1, Thrust/1
  Gain/1 -> Sum/3
  Gain1/1 -> Sum/2
  Gain2/1 -> Sum/1

== system Final_test/Kalman Filter/Subsystem1 ==
  PWM : Inport
  Math Function1 : Math  Operator=pow  SaturateOnIntegerOverflow=on
  Product1 : Product
  Sum1 : Sum  Inputs=|++
  a : Constant  Value=0.3933
  b : Gain  Gain=0.03432
  c : Constant  Value=0.005561
  u : Outport
  wires:
  Sum1/1 -> Product1/2
  Product1/1 -> u/1
  a/1 -> Math Function1/2
  b/1 -> Sum1/1
  PWM/1 -> Math Function1/1, Product1/1
  Math Function1/1 -> b/1
  c/1 -> Sum1/2

== system Final_test/Output/If Action Subsystem ==
  In1 : Inport
  Action Port : ActionPort  ActionType=then
  Cast : DataTypeConversion  OutDataTypeStr=boolean
  Stop Simulation : Stop
  Out1 : Outport
  wires:
  In1/1 -> Cast/1, Out1/1
  Cast/1 -> Stop Simulation/1

== system Final_test/Output/If Action Subsystem1 ==
  In1 : Inport
  Action Port : ActionPort  ActionType=else
  Out1 : Outport
  wires:
  In1/1 -> Out1/1

== system Final_test/Thrust Model/Subsystem ==
  Inport1 : Inport
  Math Function1 : Math  Operator=pow  SaturateOnIntegerOverflow=on
  Sum1 : Sum  Inputs=|++
  a : Constant  Value=.99
  b : Gain  Gain=.003
  c : Constant  Value=.057
  Out1 : Outport
  wires:
  a/1 -> Math Function1/2
  b/1 -> Sum1/1
  Inport1/1 -> Math Function1/1
  Math Function1/1 -> b/1
  Sum1/1 -> Out1/1
  c/1 -> Sum1/2

== matlab function Final_test/Kalman Filter/MATLAB Function ==
  settings: updateMethod=DISCRETE
function xest  = fcn(u, y)
persistent P xh
if isempty(P)
    P = eye(2);
    xh = zeros(2,1);
end
% A = [0 1; -4 -3];
% B = [0; 4];
% C = [1 0];

Ad = [0.9998  0.009851; -0.0394    0.9702];
Bd = [0.000198; 0.0394];
Cd = [1 0];

Q = 1;
R = diag([5,5]);

% Model information
xh_bar = Ad * xh + Bd * u;
P_bar = Ad * P * Ad' + R;

% Measurement update
K = P_bar * Cd' * (Cd * P_bar * Cd' + Q)^-1;
xh = xh_bar + K * (y - Cd * xh_bar);
P = (1 - K * Cd) * P_bar;

xest = xh;
